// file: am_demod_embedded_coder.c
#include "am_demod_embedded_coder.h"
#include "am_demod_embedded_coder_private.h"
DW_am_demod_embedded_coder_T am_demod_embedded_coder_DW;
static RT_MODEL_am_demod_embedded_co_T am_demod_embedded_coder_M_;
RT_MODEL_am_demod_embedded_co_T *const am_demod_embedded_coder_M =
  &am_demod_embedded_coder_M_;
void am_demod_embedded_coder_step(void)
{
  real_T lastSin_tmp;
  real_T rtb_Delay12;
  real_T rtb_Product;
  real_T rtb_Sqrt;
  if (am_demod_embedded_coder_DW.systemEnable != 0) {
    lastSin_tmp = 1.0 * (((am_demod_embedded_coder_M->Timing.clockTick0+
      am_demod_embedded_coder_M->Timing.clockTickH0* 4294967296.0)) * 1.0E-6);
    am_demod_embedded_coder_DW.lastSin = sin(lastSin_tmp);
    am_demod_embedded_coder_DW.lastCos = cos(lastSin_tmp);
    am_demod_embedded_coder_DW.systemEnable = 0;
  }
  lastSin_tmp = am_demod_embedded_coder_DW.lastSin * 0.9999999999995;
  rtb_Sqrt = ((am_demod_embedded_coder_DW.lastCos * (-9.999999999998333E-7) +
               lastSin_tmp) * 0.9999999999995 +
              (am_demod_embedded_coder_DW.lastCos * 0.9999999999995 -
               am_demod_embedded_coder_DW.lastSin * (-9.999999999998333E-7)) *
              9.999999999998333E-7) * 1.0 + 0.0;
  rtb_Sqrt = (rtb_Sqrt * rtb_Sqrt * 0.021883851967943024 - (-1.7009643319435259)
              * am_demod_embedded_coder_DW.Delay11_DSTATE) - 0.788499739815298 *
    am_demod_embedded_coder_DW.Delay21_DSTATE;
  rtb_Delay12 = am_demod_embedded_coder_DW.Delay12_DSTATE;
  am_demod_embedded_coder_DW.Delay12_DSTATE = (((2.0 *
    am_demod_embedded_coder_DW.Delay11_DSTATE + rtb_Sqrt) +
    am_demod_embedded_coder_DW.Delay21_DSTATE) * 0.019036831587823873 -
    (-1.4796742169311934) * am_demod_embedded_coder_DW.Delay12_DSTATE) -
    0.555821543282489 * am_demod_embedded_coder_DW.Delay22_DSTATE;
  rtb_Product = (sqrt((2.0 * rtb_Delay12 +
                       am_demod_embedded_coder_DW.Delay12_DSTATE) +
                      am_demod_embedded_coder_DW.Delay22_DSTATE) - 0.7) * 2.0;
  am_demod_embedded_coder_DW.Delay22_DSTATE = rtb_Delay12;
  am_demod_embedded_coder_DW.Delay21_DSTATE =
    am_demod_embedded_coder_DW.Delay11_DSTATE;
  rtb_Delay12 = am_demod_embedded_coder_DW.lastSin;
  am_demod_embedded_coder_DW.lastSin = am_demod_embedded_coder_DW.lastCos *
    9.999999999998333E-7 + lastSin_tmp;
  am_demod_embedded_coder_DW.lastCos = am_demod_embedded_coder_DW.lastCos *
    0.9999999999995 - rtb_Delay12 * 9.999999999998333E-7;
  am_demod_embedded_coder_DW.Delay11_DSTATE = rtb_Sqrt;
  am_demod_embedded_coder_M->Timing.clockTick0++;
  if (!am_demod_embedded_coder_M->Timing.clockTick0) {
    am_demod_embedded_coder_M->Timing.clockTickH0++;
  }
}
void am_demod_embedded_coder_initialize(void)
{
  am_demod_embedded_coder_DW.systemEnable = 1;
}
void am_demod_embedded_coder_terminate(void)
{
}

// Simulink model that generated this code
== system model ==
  Product : Product  <- 1: Sum#1, 2: Constant#1
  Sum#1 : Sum  Inputs=+-  <- 1: Sqrt, 2: Constant#2
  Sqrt : Sqrt  <- 1: Sum#2
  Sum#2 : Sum  Inputs=++  <- 1: Sum#3, 2: Delay22
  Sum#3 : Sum  Inputs=++  <- 1: Sum#4, 2: Gain#1
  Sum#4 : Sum  Inputs=+-  <- 1: Sum#5, 2: Gain#2
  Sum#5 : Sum  Inputs=+-  <- 1: Gain#3, 2: Gain#4
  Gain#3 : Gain  Gain=0.0190368315878238735  <- 1: Sum#6
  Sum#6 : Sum  Inputs=++  <- 1: Sum#7, 2: Delay21
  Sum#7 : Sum  Inputs=++  <- 1: Sum#8, 2: Gain#5
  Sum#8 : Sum  Inputs=+-  <- 1: Sum#9, 2: Gain#6
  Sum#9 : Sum  Inputs=+-  <- 1: Gain#7, 2: Gain#8
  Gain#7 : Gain  Gain=0.0218838519679430236  <- 1: Product#1
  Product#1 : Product  <- 1: Sin#1, 2: Sin#1
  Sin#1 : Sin
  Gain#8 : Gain  Gain=-1.70096433194352592  <- 1: Delay11
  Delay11 : Delay  DelayLength=1  InitialCondition=0  <- 1: Sum#8
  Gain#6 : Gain  Gain=0.788499739815297973  <- 1: Delay21
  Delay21 : Delay  DelayLength=1  InitialCondition=0  <- 1: Delay11
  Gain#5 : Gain  Gain=2  <- 1: Delay11
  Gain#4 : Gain  Gain=-1.47967421693119339  <- 1: Delay12
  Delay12 : Delay  DelayLength=1  InitialCondition=0  <- 1: Sum#4
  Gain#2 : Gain  Gain=0.555821543282489006  <- 1: Delay22
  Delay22 : Delay  DelayLength=1  InitialCondition=0  <- 1: Delay12
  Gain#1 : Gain  Gain=2  <- 1: Delay12
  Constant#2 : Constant  Value=0.7
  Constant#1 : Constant  Value=2
